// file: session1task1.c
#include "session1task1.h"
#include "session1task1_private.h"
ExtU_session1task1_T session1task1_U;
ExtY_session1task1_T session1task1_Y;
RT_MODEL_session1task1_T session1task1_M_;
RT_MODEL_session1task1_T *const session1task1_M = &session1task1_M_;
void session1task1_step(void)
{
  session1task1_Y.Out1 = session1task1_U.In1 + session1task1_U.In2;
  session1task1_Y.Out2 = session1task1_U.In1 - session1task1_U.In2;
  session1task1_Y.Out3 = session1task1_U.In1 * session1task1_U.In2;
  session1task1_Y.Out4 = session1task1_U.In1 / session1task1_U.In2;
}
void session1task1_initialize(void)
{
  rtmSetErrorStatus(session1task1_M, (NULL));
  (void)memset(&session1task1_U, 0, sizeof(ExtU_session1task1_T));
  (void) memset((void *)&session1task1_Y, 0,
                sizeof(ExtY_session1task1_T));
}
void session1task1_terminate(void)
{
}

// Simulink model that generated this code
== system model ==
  In1 : Inport
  In2 : Inport
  Out1 : Outport  <- 1: Sum#1
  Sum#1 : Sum  <- 1: In1, 2: In2
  Out2 : Outport  <- 1: Sum#2
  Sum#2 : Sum  Inputs=+-  <- 1: In1, 2: In2
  Out3 : Outport  <- 1: Product#1
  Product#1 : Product  <- 1: In1, 2: In2
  Out4 : Outport  <- 1: Product#2
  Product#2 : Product  Inputs=*/  <- 1: In1, 2: In2
